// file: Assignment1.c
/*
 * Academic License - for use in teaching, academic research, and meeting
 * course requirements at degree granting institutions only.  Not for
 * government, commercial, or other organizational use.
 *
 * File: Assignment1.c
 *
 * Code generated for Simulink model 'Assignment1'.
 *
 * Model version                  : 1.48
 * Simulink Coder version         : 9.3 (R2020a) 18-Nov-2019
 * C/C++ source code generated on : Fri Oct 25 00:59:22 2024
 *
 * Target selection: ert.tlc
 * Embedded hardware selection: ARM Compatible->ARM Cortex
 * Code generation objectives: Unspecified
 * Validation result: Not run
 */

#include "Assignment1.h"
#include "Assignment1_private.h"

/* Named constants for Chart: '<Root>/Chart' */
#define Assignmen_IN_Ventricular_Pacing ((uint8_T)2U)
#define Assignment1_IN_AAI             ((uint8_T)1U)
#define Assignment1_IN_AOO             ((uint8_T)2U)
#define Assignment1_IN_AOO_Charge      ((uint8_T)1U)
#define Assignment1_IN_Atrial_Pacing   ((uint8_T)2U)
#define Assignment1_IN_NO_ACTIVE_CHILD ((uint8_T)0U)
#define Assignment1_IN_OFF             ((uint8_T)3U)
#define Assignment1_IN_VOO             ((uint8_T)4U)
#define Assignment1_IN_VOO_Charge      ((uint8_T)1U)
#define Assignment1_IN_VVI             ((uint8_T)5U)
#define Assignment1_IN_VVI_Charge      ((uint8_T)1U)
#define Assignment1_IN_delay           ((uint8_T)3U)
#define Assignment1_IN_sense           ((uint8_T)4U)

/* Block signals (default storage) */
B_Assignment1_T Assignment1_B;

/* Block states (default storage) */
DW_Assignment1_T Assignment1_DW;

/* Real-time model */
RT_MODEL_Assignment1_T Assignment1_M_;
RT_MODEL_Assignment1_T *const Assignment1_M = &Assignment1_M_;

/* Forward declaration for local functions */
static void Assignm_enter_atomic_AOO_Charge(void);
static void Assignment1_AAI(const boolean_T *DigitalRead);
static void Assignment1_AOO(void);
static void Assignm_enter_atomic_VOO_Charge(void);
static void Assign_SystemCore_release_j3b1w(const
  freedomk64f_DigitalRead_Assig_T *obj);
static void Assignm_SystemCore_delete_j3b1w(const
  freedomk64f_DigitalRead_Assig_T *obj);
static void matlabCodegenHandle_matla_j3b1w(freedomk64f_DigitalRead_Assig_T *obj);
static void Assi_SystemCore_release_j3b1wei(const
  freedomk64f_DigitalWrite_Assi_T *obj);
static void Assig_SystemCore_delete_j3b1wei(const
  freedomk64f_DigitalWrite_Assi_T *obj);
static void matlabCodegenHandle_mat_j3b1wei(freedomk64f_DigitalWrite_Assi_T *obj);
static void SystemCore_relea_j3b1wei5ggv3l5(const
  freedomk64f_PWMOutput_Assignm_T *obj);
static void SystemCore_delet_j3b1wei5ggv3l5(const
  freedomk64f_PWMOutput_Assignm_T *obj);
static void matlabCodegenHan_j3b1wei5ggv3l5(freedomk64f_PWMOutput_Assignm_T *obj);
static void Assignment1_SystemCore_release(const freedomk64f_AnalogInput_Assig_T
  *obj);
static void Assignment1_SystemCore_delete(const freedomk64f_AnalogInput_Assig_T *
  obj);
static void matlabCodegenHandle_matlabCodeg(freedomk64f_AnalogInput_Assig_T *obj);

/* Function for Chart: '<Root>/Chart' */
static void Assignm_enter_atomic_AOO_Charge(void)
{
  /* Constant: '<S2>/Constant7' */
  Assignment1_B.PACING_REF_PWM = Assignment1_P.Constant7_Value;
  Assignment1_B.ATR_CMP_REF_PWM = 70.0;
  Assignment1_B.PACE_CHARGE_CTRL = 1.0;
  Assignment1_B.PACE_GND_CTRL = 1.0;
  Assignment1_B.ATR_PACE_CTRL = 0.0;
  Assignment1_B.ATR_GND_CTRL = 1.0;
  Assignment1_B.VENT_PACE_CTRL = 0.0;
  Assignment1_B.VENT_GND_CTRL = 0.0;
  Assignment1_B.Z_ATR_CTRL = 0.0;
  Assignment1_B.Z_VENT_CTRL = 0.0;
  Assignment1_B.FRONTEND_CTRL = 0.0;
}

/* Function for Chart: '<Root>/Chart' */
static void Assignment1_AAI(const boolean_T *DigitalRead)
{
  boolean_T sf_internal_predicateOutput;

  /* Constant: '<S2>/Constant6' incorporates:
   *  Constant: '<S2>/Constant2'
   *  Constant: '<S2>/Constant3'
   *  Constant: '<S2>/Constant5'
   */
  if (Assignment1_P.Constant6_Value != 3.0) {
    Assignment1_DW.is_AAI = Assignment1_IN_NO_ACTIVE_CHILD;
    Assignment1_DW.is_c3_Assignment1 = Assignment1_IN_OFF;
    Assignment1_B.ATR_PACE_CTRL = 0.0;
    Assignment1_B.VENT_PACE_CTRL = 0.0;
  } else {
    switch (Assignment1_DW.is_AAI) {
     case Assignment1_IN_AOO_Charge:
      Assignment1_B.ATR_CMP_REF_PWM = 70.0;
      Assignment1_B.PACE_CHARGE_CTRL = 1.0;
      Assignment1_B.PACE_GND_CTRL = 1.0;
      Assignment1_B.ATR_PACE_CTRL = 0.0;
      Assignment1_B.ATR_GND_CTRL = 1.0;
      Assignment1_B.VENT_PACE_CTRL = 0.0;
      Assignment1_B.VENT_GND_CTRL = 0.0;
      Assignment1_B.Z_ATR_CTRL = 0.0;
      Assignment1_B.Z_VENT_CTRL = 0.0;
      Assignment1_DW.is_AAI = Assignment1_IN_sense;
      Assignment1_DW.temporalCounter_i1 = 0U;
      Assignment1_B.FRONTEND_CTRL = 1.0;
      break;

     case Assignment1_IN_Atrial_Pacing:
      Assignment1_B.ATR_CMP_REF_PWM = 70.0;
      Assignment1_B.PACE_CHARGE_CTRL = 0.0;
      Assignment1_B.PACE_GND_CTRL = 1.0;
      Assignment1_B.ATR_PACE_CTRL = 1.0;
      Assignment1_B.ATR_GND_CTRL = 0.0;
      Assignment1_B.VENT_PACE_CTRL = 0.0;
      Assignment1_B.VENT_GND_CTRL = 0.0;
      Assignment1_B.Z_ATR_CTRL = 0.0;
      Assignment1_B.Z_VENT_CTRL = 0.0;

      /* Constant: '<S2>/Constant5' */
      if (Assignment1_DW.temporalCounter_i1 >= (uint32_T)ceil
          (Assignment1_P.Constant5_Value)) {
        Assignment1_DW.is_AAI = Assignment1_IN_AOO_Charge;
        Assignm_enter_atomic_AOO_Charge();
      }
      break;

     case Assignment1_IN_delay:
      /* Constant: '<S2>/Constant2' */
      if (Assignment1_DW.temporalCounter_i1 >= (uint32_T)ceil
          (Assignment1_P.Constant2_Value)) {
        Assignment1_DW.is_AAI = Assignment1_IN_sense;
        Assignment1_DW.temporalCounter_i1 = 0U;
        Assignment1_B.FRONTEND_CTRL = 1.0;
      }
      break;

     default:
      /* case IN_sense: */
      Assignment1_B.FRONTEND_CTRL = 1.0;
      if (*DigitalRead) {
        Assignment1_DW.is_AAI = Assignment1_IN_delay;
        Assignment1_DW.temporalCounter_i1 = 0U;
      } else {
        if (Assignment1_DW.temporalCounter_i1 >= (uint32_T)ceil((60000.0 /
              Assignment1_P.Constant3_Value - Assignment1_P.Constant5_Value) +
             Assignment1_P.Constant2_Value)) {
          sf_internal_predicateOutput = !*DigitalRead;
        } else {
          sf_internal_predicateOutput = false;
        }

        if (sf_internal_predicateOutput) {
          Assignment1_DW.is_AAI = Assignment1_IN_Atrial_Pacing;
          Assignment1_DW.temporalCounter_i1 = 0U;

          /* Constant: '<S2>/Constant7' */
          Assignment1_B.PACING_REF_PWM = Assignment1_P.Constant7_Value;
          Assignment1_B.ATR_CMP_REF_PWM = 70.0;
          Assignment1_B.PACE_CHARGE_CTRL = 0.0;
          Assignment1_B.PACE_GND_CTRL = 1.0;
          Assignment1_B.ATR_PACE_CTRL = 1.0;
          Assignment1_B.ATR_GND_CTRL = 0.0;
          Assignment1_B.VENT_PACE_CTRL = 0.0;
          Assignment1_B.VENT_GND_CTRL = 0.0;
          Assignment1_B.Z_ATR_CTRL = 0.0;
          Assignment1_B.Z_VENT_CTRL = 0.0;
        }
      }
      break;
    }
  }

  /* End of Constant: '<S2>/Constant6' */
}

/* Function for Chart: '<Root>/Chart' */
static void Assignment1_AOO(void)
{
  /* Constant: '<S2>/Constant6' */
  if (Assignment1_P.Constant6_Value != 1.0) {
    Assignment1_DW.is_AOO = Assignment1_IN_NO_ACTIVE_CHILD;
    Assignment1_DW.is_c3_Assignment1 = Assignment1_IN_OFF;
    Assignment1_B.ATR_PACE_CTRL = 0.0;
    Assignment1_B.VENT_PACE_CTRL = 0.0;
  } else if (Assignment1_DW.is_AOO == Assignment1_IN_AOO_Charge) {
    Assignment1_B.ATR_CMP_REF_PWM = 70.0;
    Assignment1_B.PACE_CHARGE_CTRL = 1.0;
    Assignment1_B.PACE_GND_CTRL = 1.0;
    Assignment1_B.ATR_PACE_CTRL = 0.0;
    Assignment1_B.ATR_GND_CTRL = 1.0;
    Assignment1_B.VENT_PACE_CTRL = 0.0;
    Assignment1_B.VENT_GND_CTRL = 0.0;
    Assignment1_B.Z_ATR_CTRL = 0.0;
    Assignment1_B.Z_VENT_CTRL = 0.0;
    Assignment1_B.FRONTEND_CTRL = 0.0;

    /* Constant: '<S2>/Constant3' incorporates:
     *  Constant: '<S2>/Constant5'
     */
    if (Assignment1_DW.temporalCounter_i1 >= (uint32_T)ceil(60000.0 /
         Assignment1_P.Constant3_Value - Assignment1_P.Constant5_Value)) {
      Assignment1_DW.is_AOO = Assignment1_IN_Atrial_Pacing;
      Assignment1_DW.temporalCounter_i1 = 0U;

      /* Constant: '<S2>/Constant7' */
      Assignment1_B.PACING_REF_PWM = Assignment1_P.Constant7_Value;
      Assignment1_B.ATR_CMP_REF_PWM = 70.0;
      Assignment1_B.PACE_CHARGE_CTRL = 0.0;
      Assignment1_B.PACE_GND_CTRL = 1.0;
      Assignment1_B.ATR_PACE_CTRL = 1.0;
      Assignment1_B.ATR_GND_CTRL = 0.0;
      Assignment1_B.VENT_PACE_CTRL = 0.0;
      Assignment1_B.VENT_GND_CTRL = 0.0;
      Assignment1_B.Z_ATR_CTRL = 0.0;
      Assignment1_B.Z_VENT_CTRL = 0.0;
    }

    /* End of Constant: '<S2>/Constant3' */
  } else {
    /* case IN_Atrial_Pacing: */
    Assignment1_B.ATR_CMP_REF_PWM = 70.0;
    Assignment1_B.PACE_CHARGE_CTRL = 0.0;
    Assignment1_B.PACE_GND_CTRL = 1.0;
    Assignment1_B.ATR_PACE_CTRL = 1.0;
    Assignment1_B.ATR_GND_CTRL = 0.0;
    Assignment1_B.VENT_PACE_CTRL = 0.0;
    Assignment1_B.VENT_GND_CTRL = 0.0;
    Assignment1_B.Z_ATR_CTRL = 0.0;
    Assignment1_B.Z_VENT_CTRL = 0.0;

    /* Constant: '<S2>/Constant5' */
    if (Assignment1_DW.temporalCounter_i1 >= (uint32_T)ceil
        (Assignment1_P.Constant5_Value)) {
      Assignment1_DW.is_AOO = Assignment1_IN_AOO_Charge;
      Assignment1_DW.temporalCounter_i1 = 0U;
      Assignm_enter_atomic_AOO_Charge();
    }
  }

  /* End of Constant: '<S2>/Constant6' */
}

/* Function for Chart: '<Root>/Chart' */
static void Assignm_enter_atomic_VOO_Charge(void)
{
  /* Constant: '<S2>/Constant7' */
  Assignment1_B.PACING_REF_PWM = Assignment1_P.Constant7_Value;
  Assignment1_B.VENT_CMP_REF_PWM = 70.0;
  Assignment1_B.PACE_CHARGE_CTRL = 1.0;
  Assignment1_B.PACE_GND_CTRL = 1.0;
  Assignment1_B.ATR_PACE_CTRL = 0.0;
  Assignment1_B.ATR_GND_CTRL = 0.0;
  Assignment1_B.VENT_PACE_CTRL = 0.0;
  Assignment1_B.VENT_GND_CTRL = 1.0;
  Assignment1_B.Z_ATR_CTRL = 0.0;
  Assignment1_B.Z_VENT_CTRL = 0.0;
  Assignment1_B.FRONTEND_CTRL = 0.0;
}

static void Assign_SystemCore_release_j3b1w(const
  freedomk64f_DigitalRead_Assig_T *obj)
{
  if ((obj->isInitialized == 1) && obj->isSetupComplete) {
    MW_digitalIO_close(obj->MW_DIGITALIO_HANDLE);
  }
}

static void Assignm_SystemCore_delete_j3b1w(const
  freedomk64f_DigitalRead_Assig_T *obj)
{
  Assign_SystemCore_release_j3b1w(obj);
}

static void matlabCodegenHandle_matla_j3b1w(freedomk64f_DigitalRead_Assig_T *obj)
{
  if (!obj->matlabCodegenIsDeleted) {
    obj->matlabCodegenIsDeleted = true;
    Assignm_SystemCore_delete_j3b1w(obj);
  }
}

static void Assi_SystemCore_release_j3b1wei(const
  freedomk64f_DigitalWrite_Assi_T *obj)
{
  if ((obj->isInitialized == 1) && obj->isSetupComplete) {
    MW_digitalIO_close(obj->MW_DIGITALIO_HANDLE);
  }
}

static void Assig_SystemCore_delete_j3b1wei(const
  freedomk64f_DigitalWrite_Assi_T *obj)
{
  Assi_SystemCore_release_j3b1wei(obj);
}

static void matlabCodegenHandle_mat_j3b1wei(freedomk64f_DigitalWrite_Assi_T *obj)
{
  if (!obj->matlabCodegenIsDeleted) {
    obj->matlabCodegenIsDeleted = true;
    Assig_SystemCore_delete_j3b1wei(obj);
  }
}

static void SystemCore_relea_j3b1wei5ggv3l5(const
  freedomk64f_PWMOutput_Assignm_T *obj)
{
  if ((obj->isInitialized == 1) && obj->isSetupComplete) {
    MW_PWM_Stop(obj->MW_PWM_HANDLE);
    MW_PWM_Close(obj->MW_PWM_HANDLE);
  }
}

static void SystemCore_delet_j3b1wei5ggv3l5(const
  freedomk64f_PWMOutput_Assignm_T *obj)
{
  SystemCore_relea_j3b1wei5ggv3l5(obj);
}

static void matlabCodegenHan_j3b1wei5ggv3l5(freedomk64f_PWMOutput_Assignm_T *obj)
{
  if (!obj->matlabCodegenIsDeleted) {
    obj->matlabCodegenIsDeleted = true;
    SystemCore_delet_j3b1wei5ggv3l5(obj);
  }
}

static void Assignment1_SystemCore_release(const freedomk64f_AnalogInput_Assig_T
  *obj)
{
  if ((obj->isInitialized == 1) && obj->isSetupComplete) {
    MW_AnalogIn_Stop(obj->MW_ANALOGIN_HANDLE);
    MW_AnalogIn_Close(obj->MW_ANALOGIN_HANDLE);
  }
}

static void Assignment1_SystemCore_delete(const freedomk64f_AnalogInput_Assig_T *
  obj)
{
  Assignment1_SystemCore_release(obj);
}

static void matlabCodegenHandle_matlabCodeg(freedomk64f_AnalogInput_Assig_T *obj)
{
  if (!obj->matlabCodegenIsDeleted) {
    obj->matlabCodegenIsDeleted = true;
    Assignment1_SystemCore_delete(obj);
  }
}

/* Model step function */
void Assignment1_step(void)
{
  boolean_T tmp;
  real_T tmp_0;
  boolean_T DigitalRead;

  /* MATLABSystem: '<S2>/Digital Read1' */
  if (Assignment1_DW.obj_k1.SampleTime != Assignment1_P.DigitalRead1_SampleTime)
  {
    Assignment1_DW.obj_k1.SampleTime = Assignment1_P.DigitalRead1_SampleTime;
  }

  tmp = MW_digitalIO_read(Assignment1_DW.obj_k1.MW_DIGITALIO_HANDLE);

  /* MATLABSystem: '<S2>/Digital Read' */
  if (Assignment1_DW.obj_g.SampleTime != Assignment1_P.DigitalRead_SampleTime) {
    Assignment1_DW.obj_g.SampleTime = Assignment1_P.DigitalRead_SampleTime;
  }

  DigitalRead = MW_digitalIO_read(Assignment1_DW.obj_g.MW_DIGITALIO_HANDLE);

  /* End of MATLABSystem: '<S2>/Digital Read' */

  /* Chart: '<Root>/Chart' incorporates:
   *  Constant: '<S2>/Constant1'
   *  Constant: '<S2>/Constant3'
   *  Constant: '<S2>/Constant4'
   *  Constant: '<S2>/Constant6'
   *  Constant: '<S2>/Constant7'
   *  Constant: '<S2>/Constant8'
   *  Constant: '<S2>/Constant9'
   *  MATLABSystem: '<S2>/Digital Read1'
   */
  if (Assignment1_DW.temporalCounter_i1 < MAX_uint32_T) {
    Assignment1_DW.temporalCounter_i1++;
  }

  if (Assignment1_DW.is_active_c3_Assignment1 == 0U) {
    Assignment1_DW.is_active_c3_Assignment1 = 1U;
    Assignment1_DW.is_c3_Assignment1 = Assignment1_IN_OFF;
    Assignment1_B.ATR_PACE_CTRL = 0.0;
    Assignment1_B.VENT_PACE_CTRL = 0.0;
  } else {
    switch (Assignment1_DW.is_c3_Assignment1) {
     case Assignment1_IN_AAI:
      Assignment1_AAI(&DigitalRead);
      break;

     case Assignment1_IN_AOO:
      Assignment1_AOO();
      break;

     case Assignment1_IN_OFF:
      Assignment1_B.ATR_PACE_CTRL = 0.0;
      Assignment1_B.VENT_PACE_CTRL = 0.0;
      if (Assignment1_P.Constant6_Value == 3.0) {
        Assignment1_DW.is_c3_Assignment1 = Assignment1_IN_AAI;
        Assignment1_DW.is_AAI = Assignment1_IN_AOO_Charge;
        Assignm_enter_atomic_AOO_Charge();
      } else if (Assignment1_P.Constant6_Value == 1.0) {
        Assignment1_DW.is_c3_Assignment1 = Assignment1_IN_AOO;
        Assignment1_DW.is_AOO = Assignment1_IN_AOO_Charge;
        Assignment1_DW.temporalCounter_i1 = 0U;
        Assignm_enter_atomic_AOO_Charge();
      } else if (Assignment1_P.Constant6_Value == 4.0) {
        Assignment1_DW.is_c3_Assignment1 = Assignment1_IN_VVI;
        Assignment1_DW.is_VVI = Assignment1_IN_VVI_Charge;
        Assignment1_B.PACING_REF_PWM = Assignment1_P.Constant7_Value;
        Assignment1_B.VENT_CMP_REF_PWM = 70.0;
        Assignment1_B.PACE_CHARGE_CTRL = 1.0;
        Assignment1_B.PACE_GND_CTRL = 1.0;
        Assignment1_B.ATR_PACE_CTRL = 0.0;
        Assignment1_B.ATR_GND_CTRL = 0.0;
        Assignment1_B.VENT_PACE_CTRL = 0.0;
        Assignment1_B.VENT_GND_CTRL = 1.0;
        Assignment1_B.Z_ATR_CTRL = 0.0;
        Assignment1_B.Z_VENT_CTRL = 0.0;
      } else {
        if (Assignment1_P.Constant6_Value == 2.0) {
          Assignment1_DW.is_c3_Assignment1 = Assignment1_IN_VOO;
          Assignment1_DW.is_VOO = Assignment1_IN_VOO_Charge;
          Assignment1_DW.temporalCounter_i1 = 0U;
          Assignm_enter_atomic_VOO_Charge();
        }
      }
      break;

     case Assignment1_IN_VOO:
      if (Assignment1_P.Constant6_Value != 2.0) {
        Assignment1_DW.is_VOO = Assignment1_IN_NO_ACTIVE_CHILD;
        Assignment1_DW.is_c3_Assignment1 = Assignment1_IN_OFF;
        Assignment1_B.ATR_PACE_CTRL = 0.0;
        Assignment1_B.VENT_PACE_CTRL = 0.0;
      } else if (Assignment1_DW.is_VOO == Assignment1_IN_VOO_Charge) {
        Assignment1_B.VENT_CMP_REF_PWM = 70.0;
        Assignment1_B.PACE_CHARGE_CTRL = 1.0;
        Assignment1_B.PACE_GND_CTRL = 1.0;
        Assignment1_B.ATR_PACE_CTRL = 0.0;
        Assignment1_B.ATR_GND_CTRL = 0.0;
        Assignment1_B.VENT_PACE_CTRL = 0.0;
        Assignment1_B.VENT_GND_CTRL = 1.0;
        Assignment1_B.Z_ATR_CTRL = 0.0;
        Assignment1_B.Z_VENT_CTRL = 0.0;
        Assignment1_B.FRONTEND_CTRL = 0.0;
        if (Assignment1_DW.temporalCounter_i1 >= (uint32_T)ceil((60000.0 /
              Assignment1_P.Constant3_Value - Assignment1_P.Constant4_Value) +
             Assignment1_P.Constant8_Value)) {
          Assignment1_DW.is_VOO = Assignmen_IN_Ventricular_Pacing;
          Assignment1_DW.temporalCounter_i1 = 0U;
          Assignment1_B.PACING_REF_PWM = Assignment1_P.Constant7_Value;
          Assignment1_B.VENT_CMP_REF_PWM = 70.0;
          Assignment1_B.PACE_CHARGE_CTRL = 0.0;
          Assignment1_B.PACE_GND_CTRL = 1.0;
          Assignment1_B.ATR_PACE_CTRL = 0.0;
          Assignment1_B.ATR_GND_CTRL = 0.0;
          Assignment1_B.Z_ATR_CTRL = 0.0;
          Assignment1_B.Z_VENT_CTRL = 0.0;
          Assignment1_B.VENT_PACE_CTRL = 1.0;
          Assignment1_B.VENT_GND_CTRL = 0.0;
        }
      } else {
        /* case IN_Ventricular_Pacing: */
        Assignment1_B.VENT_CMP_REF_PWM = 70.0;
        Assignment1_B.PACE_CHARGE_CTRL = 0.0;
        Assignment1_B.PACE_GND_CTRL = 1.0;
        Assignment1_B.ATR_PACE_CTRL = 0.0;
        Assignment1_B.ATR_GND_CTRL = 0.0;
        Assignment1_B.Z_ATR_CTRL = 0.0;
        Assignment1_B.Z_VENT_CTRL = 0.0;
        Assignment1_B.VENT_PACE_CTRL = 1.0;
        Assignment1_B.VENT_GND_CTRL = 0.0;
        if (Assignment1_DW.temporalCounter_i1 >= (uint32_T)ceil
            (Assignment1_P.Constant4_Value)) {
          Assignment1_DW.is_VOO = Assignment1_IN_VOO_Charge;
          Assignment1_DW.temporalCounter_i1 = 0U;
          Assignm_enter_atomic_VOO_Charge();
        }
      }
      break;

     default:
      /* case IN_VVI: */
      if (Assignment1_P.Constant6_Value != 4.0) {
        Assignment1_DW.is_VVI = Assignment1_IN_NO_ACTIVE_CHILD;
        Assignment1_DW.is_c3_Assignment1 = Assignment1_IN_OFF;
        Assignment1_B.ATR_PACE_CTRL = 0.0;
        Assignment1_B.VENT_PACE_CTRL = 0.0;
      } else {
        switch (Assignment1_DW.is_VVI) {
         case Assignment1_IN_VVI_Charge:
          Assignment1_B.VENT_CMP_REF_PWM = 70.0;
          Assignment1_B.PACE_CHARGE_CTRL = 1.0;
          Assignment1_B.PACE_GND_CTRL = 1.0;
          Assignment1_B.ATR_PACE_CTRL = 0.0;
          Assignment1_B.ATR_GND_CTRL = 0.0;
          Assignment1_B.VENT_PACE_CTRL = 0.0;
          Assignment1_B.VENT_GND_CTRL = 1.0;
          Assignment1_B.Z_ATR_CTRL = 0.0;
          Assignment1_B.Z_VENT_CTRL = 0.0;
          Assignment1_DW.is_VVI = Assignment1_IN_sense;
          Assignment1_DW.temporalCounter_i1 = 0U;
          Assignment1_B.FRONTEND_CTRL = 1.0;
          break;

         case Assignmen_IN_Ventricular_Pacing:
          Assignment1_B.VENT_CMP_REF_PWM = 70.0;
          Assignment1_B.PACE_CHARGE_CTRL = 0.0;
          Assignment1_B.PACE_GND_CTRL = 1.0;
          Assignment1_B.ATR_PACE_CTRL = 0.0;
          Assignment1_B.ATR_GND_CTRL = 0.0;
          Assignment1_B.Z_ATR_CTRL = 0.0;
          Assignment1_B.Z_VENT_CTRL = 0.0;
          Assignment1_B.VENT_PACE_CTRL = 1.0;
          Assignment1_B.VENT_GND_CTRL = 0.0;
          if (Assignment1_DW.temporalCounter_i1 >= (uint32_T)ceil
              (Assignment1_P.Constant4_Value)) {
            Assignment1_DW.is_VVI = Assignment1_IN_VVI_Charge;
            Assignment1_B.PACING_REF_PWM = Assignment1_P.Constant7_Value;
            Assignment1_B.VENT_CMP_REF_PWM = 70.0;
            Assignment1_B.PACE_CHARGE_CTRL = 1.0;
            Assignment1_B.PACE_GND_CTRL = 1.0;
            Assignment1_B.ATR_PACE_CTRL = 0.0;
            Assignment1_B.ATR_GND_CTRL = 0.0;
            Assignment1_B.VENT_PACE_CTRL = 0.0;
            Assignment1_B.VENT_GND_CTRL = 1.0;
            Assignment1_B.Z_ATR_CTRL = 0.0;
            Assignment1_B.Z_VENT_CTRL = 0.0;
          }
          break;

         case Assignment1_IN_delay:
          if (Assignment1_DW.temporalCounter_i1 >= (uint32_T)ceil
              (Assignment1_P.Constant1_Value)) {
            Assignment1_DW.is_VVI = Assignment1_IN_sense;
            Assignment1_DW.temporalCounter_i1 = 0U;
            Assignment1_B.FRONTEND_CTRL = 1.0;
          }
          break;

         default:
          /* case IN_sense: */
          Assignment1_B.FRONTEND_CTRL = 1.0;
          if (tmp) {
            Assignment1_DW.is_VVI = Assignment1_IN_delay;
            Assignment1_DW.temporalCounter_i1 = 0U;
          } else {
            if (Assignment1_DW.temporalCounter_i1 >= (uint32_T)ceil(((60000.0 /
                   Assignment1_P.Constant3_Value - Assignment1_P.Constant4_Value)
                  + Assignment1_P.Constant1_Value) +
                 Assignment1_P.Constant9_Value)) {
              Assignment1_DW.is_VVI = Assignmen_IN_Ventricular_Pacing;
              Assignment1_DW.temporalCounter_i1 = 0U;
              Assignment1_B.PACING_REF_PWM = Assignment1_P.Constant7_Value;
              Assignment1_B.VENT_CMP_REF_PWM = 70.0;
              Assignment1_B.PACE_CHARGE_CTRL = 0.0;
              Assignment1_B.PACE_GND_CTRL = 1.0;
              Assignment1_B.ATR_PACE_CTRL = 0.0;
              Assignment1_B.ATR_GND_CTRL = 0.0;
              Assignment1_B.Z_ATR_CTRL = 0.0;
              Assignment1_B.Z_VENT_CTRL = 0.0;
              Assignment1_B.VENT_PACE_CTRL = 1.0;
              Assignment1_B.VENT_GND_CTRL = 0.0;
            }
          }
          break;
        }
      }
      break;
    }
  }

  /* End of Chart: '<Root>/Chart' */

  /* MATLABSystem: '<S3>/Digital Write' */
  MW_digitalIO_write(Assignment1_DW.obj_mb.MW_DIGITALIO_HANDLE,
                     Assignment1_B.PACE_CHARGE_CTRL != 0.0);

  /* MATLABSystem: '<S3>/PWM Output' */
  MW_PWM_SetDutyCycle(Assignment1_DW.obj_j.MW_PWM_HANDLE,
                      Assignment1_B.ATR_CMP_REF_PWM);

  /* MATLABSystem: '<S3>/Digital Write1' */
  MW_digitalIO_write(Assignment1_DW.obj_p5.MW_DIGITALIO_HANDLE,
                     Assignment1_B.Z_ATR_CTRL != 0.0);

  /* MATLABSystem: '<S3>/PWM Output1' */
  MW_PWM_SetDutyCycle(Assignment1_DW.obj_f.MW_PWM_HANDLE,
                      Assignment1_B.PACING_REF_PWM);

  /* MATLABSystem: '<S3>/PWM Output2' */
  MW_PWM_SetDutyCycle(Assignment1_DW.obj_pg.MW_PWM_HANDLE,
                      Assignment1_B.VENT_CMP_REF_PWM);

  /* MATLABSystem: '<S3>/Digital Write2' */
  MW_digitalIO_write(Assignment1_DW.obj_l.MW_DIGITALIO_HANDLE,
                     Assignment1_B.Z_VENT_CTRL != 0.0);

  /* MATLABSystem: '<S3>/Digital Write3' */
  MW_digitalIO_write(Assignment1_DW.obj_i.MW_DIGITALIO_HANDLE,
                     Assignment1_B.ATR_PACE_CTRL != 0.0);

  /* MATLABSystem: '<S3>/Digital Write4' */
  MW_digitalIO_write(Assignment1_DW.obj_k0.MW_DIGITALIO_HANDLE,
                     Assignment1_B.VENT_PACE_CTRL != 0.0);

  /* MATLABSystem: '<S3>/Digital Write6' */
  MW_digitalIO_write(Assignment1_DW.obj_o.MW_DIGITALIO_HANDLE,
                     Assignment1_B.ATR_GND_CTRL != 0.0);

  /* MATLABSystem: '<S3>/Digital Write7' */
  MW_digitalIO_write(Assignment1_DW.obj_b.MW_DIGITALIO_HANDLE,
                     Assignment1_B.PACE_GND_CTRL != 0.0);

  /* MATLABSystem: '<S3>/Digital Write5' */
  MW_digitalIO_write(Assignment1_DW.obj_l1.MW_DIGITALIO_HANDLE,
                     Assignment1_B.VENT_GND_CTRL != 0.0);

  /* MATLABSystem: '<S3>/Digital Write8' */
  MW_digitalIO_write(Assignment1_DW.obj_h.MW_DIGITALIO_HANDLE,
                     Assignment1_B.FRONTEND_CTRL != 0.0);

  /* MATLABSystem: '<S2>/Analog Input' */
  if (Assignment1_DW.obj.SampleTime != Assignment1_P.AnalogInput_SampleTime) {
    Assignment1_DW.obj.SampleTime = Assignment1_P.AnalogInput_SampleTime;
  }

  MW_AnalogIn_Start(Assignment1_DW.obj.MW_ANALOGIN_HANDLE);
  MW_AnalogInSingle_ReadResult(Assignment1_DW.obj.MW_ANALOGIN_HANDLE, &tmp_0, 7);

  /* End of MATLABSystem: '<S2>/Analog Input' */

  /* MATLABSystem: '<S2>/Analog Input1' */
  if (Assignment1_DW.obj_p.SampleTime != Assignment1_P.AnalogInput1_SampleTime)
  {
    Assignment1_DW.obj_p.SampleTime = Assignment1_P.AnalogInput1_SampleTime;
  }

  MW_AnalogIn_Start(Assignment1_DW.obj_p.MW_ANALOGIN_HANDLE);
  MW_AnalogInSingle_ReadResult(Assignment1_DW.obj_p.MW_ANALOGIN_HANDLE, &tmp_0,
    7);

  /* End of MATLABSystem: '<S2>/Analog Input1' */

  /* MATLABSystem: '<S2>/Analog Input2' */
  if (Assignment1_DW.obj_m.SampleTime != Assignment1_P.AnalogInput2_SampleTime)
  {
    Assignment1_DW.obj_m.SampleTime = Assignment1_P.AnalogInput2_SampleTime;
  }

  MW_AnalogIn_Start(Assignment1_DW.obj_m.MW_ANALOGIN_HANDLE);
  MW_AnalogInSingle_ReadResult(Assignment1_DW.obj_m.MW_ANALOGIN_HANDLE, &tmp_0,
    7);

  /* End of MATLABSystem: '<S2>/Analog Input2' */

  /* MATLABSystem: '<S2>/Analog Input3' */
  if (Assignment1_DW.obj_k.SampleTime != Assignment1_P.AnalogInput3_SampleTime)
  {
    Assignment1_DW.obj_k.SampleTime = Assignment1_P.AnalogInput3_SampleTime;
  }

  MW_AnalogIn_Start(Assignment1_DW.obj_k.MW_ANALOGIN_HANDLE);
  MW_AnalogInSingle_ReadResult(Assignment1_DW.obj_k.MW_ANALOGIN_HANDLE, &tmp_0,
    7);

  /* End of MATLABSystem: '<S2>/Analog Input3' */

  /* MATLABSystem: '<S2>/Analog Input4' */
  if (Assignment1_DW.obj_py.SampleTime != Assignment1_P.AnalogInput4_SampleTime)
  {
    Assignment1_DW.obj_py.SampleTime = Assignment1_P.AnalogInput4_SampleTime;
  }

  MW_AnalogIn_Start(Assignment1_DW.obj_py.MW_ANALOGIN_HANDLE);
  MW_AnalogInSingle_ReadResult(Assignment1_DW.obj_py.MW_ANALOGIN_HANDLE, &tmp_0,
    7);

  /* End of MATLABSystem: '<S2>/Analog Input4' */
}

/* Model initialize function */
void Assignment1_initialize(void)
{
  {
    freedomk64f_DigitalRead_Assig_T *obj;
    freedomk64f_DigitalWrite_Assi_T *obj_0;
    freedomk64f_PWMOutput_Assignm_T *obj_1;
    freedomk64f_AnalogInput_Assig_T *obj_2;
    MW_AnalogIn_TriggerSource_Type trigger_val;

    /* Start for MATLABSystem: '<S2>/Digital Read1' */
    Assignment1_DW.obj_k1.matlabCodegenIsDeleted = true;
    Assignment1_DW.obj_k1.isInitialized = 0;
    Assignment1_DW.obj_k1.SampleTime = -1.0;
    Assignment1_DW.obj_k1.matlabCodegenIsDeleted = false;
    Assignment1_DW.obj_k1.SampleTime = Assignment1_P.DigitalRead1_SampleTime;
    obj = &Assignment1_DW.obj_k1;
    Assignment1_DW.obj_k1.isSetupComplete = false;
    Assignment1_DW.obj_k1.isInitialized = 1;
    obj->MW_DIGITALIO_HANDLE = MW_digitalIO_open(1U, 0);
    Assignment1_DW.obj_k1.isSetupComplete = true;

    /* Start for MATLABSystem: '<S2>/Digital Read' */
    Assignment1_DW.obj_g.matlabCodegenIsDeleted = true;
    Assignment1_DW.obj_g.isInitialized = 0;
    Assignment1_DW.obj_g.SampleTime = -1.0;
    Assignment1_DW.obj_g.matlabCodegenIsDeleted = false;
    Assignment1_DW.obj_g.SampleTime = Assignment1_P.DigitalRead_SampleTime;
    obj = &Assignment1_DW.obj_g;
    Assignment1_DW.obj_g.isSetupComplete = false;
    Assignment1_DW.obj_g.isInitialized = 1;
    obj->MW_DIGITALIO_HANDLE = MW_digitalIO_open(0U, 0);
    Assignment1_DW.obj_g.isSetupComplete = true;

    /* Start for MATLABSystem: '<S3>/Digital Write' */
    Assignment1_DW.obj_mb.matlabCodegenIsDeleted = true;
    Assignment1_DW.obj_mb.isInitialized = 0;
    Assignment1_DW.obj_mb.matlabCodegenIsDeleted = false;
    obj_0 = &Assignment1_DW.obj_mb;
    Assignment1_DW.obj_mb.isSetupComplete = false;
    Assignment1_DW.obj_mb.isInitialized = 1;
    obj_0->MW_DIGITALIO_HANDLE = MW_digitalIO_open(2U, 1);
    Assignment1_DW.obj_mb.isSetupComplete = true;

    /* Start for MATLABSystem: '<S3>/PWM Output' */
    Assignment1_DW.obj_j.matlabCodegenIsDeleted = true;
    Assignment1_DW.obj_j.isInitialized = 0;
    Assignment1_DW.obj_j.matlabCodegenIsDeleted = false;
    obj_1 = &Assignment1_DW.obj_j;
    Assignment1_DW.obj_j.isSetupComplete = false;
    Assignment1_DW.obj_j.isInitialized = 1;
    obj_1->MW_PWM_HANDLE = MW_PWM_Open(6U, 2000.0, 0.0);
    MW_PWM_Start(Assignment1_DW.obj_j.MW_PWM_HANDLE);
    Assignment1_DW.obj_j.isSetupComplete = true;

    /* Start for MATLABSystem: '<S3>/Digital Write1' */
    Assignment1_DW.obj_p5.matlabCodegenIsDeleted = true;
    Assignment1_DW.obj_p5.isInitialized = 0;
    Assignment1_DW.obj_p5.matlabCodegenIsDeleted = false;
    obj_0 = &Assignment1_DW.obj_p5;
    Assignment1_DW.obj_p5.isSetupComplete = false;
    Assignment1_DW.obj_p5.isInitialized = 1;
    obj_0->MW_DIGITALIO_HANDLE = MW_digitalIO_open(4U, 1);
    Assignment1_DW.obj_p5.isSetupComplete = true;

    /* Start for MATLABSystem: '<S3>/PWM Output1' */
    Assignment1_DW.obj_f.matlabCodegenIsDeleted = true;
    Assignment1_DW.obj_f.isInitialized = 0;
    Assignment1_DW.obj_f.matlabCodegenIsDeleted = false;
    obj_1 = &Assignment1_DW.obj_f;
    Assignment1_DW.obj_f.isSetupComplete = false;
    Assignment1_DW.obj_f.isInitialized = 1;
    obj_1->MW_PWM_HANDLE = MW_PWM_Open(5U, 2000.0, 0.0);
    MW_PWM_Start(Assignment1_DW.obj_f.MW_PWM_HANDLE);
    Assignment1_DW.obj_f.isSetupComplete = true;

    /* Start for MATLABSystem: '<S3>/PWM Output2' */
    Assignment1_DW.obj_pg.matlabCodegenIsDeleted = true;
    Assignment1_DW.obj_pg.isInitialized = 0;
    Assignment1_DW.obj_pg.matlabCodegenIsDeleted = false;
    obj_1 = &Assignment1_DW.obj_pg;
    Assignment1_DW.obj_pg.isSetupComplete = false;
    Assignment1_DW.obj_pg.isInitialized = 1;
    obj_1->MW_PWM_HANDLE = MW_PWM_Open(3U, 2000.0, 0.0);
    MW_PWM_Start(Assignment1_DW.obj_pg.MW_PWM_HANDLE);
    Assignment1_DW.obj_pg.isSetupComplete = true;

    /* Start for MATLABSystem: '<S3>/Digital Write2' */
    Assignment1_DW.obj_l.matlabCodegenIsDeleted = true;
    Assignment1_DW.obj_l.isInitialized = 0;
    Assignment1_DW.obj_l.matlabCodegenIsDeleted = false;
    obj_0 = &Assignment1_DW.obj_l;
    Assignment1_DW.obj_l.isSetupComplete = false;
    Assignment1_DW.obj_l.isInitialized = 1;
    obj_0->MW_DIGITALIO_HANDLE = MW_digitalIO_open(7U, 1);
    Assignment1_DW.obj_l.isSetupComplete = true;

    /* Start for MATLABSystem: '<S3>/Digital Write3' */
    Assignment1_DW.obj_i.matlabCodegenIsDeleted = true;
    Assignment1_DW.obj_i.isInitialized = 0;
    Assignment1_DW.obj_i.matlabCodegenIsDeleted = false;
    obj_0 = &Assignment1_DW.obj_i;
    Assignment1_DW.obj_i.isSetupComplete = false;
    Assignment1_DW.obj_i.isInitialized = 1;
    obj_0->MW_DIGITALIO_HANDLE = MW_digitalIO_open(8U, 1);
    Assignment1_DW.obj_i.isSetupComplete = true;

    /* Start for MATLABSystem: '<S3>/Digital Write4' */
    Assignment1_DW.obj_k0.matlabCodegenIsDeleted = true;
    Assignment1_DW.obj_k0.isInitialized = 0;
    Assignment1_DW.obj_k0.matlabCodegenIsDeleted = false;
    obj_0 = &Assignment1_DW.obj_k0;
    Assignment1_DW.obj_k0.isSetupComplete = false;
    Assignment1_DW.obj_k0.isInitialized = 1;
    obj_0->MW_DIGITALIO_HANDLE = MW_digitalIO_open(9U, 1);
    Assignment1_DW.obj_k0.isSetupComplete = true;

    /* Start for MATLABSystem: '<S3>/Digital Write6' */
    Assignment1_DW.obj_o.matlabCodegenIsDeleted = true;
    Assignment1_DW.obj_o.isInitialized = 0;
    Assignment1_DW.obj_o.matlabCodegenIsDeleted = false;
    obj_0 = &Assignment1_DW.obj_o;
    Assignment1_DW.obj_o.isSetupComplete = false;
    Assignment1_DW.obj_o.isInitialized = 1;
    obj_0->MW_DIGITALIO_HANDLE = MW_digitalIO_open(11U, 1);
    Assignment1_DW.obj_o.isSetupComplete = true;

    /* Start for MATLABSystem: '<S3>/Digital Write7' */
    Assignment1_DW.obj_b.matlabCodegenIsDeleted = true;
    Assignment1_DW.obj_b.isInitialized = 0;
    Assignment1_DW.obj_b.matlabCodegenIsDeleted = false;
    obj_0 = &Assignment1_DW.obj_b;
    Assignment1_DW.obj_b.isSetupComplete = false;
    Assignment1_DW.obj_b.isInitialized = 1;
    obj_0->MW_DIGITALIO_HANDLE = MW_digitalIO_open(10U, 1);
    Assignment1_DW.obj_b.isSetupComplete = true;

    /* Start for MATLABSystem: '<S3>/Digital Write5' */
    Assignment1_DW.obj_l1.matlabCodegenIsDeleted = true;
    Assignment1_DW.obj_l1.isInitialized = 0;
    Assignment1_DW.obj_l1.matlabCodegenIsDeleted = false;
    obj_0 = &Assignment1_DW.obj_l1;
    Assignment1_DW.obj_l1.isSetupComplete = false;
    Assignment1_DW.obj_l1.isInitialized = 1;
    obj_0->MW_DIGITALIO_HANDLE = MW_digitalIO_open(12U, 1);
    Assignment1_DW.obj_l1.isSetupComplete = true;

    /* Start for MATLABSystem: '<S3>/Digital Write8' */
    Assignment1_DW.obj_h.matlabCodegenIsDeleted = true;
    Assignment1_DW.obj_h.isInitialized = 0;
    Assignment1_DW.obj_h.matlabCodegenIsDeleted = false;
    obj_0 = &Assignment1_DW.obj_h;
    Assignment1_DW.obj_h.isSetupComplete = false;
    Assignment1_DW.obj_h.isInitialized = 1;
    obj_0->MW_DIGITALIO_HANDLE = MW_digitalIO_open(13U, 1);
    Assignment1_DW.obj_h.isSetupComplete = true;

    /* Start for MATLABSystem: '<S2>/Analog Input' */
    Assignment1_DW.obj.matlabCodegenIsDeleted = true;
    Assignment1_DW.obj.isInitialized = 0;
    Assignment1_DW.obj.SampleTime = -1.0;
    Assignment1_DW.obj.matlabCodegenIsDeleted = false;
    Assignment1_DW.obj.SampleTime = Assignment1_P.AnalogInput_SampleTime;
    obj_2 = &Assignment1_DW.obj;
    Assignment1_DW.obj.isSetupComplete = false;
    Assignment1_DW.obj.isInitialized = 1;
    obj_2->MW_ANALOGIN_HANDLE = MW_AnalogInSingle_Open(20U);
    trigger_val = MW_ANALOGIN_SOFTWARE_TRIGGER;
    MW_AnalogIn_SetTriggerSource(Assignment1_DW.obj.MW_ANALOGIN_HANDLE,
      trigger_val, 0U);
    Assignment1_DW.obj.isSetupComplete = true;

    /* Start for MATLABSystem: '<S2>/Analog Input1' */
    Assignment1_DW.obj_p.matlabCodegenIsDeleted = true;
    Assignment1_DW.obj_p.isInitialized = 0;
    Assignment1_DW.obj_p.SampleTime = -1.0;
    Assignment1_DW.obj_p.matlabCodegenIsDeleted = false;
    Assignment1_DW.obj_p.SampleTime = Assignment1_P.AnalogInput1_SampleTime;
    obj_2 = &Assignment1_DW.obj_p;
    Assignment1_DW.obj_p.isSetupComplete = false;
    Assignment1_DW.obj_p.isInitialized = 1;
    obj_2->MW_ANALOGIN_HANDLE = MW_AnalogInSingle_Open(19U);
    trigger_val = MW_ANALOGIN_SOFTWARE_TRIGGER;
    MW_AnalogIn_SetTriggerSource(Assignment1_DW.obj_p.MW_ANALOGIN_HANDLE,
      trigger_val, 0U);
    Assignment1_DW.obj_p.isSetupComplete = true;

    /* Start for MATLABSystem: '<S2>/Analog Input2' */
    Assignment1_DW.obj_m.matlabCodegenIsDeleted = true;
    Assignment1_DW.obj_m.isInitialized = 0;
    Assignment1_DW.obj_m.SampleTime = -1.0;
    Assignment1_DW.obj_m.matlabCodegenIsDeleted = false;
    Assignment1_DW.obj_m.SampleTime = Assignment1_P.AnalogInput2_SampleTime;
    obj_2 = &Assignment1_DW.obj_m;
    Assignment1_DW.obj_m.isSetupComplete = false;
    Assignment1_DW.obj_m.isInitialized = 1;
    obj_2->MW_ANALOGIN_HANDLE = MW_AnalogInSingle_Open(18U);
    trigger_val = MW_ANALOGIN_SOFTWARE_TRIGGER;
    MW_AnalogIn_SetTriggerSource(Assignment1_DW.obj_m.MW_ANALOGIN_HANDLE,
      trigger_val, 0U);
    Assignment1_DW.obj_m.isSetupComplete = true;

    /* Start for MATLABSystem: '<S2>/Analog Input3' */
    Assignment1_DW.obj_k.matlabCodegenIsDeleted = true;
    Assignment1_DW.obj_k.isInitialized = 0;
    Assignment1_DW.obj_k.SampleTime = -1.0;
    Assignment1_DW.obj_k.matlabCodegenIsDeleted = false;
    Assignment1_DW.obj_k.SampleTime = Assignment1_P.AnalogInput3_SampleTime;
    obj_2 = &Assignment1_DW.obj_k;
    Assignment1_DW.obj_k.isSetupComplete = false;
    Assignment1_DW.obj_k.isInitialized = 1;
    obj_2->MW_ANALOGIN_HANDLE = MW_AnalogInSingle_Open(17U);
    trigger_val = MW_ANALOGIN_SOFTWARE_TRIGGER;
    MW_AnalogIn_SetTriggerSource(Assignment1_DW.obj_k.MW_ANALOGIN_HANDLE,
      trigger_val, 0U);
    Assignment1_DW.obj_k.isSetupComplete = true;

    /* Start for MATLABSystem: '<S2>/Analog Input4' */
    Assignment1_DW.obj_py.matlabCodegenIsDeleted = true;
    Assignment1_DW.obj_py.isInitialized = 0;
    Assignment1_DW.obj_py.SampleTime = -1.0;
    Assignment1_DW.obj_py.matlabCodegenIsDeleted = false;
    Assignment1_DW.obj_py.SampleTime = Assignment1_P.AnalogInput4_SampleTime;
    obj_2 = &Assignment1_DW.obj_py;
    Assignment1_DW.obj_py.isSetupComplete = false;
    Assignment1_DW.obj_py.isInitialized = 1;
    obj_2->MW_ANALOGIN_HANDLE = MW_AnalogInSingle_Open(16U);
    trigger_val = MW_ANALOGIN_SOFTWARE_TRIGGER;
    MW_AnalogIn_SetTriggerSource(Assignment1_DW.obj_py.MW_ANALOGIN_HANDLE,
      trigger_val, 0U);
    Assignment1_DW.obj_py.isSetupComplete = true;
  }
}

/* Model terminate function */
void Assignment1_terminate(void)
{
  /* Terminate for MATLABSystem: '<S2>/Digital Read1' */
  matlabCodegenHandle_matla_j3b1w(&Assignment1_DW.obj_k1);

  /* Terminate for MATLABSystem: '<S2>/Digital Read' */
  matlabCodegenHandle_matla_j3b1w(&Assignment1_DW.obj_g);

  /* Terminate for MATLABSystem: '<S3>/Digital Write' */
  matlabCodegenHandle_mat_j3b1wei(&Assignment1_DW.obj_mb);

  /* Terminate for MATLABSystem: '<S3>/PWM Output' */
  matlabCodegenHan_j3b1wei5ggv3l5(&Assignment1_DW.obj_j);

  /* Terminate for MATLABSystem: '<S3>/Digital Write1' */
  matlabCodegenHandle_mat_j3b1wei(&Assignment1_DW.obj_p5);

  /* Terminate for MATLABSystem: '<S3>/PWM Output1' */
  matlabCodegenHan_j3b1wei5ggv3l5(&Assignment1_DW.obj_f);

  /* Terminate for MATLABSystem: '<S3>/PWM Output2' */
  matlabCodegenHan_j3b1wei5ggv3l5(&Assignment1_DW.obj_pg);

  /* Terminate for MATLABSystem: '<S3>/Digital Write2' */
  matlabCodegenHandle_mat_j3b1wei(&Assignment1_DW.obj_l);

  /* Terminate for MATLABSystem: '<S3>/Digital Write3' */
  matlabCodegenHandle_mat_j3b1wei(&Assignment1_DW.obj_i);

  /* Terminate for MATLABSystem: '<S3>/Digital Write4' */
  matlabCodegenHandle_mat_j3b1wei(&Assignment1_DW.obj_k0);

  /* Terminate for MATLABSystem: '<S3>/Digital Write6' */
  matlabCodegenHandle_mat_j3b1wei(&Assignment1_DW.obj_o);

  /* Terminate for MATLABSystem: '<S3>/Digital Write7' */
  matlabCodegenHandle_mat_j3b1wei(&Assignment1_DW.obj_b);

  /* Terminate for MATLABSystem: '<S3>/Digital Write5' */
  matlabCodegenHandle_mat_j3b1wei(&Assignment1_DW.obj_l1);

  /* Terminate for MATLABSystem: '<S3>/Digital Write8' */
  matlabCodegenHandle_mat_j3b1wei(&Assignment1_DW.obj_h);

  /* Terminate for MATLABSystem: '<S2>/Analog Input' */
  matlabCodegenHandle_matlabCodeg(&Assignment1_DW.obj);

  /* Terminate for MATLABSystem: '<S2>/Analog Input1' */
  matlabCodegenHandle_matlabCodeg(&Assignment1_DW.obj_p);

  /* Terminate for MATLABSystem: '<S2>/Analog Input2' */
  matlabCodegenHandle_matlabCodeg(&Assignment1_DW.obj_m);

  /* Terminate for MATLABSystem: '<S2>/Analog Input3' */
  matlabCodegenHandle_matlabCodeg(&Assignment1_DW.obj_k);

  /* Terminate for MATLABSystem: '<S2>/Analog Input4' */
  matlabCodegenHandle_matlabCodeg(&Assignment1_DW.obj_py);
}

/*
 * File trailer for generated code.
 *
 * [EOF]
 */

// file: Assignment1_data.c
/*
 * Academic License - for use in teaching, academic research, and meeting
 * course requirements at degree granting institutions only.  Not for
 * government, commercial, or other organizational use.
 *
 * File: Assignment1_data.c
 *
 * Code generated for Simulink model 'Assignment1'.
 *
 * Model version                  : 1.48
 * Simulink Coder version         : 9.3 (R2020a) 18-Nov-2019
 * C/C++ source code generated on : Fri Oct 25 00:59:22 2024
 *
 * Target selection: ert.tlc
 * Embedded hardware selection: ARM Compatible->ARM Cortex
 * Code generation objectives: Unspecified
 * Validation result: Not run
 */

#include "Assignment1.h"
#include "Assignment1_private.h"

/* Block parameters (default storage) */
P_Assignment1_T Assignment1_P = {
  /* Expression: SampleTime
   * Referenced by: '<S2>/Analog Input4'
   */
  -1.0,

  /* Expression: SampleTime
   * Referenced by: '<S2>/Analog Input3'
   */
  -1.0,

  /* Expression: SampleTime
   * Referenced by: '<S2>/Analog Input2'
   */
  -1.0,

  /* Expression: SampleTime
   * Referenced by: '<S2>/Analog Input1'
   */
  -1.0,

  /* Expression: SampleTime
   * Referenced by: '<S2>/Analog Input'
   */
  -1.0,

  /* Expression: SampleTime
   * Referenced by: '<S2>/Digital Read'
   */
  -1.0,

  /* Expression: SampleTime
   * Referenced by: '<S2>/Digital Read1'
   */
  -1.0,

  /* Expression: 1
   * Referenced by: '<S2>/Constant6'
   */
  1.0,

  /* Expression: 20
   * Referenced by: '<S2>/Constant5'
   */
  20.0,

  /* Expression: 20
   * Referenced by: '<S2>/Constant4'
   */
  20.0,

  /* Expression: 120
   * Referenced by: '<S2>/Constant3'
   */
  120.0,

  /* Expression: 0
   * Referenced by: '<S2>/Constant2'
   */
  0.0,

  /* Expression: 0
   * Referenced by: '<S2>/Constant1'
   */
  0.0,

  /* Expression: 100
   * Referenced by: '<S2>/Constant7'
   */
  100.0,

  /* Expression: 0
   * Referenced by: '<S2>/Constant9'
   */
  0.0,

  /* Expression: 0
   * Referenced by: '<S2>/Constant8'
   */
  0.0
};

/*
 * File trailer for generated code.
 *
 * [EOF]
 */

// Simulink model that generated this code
simulink model "Assignment1"  (R2020a)
settings: Solver=FixedStepAuto  StartTime=0.0  StopTime=5  FixedStep=1e-3  RelTol=1e-3  EnableMultiTasking=on
model workspace (MAT data in the model file):
  ATR_CMP_REF_PWM_PERCENTAGE = 50
  PACING_REF_PWM_DUTY_PERCENTAGE = 50
  VENT_CMP_REF_PWM_PERCENTAGE = 50
undefined symbols (not defined in the file or in its folder): A0, A1, A2, A3, A4, D0, D1, PTB10, PTB11, PTB2, PTB3, PTC11, PTC16, PTC17
libraries: frdmk64flib x7

== system Assignment1 ==
  Chart : Stateflow chart  TreatAsAtomicUnit=on
  Input : Subsystem
  Output : Subsystem  ReferencedSubsystem=k64f_subsystem
  wires:
  Input/1(mode) -> Chart/1(mode)
  Chart/10(PACING_REF_PWM) -> Output/4
  Input/2(atrial_pulse_width) -> Chart/2(atrial_pulse_width)
  Input/3(ventricular_pulse_width) -> Chart/3(ventricular_pulse_width)
  Chart/8(Z_ATR_CTRL) -> Output/3
  Chart/7(Z_VENT_CTRL) -> Output/6
  Chart/4(ATR_GND_CTRL) -> Output/9
  Chart/3(ATR_PACE_CTRL) -> Output/7
  Chart/5(VENT_GND_CTRL) -> Output/11
  Chart/2(VENT_PACE_CTRL) -> Output/8
  Chart/1(PACE_CHARGE_CTRL) -> Output/1
  Chart/6(PACE_GND_CTRL) -> Output/10
  Chart/11(ATR_CMP_REF_PWM) -> Output/2
  Chart/12(VENT_CMP_REF_PWM) -> Output/5
  Chart/9(FRONTEND_CTRL) -> Output/12
  Input/6(BPM) -> Chart/6(BPM)
  Input/4(VENT_CMP_DETECT) -> Chart/4(VENT_CMP_DETECT)
  Input/5(ATR_CMP_DETECT) -> Chart/5(ATR_CMP_DETECT)
  Input/7(ARP) -> Chart/7(ARP)
  Input/8(VRP) -> Chart/8(VRP)
  Input/9(amplitude) -> Chart/9(amplitude)
  Input/10(URL) -> Chart/10(URL)
  Input/11(LRL) -> Chart/11(LRL)

== system Assignment1/Input ==
  note: Ventricular Pins
  note: Atrial Pins
  note: Impedance Pins
  note: Parameter Pins
  Analog Input : frdmk64flib/Analog Input  Whichpin=PTC11 (A4)  SampleTime=-1
  Analog Input1 : frdmk64flib/Analog Input  Whichpin=PTB11 (A3)  SampleTime=-1
  Analog Input2 : frdmk64flib/Analog Input  Whichpin=PTB10 (A2)  SampleTime=-1
  Analog Input3 : frdmk64flib/Analog Input  Whichpin=PTB3 (A1)  SampleTime=-1
  Analog Input4 : frdmk64flib/Analog Input  Whichpin=PTB2 (A0)  SampleTime=-1
  Constant{1..2,8..9} (4 alike) : Constant  Value=0
  Constant3 : Constant  Value=120
  Constant4 : Constant  Value=20
  Constant5 : Constant  Value=20
  Constant6 : Constant
  Constant7 : Constant  Value=100
  Digital Read : frdmk64flib/Digital Read  Whichpin=PTC16 (D0)  SampleTime=-1
  Digital Read1 : frdmk64flib/Digital Read  Whichpin=PTC17 (D1)  SampleTime=-1
  mode : Outport
  atrial_pulse_width : Outport  Port=2
  ventricular_pulse_width : Outport  Port=3
  VENT_CMP_DETECT : Outport  Port=4
  ATR_CMP_DETECT : Outport  Port=5
  BPM : Outport  Port=6
  ARP : Outport  Port=7
  VRP : Outport  Port=8
  amplitude : Outport  Port=9
  URL : Outport  Port=10
  LRL : Outport  Port=11
  VENT_RECT_SIGNAL : Outport  Port=12
  ATR_RECT_SIGNAL : Outport  Port=13
  Z_SIGNAL : Outport  Port=14
  VENT_SIGNAL : Outport  Port=15
  ATR_SIGNAL : Outport  Port=16
  wires:
  Analog Input4/1 -> ATR_SIGNAL/1
  Analog Input2/1 -> Z_SIGNAL/1
  Analog Input3/1 -> VENT_SIGNAL/1
  Analog Input/1 -> VENT_RECT_SIGNAL/1
  Digital Read1/1 -> VENT_CMP_DETECT/1
  Digital Read/1 -> ATR_CMP_DETECT/1
  Analog Input1/1 -> ATR_RECT_SIGNAL/1
  Constant6/1 -> mode/1
  Constant5/1 -> atrial_pulse_width/1
  Constant4/1 -> ventricular_pulse_width/1
  Constant3/1 -> BPM/1
  Constant1/1 -> VRP/1
  Constant2/1 -> ARP/1
  Constant7/1 -> amplitude/1
  Constant9/1 -> URL/1
  Constant8/1 -> LRL/1

== stateflow chart Assignment1/Chart ==
  state AAI
    state delay
    state AOO_Charge
      entry:
      PACING_REF_PWM = amplitude;
      ATR_CMP_REF_PWM = 70;
      PACE_CHARGE_CTRL = 1;
      PACE_GND_CTRL = 1;
      ATR_PACE_CTRL = 0;
      ATR_GND_CTRL = 1;
      VENT_PACE_CTRL = 0;
      VENT_GND_CTRL = 0;
      Z_ATR_CTRL = 0;
      Z_VENT_CTRL =0;
      FRONTEND_CTRL = 0;
    state sense
      entry:
      FRONTEND_CTRL = 1;
    state Atrial_Pacing
      entry:
      PACING_REF_PWM = amplitude;
      ATR_CMP_REF_PWM = 70;
      PACE_CHARGE_CTRL = 0;
      PACE_GND_CTRL = 1;
      ATR_PACE_CTRL = 1;
      ATR_GND_CTRL = 0;
      VENT_PACE_CTRL = 0;
      VENT_GND_CTRL = 0;
      Z_ATR_CTRL = 0;
      Z_VENT_CTRL = 0;
    (default) -> AAI.AOO_Charge
    AAI.delay -> AAI.sense : [after(ARP,msec)]
    AAI.sense -> AAI.delay [order 1] : [ATR_CMP_DETECT == 1]
    AAI.AOO_Charge -> AAI.sense
    AAI.sense -> AAI.Atrial_Pacing [order 2] : [after((60000/BPM) - atrial_pulse_width + ARP,msec) && ATR_CMP_DETECT == 0]
    AAI.Atrial_Pacing -> AAI.AOO_Charge : [after(atrial_pulse_width,msec)]
  state VVI
    state delay
    state VVI_Charge
      entry:
      PACING_REF_PWM = amplitude;
      VENT_CMP_REF_PWM = 70;
      PACE_CHARGE_CTRL = 1;
      PACE_GND_CTRL = 1;
      ATR_PACE_CTRL = 0;
      ATR_GND_CTRL = 0;
      VENT_PACE_CTRL = 0;
      VENT_GND_CTRL = 1;
      Z_ATR_CTRL = 0;
      Z_VENT_CTRL =0;
    state sense
      entry:
      FRONTEND_CTRL = 1;
    state Ventricular_Pacing
      entry:
      PACING_REF_PWM = amplitude;
      VENT_CMP_REF_PWM = 70;
      PACE_CHARGE_CTRL = 0;
      PACE_GND_CTRL = 1;
      ATR_PACE_CTRL = 0;
      ATR_GND_CTRL = 0;
      Z_ATR_CTRL = 0;
      Z_VENT_CTRL = 0;
      VENT_PACE_CTRL = 1;
      VENT_GND_CTRL = 0;
    (default) -> VVI_Charge
    VVI.delay -> VVI.sense : [after(VRP,msec)]
    VVI.sense -> VVI.delay [order 1] : [VENT_CMP_DETECT == 1]
    VVI_Charge -> VVI.sense
    VVI.sense -> VVI.Ventricular_Pacing [order 2] : [after((60000/BPM) - ventricular_pulse_width + VRP + URL,msec) && VENT_CMP_DETECT == 0]
    VVI.Ventricular_Pacing -> VVI_Charge : [after(ventricular_pulse_width,msec)]
  state AOO
    state AOO_Charge
      entry:
      PACING_REF_PWM = amplitude;
      ATR_CMP_REF_PWM = 70;
      PACE_CHARGE_CTRL = 1;
      PACE_GND_CTRL = 1;
      ATR_PACE_CTRL = 0;
      ATR_GND_CTRL = 1;
      VENT_PACE_CTRL = 0;
      VENT_GND_CTRL = 0;
      Z_ATR_CTRL = 0;
      Z_VENT_CTRL =0;
      FRONTEND_CTRL = 0;
    state Atrial_Pacing
      entry:
      PACING_REF_PWM = amplitude;
      ATR_CMP_REF_PWM = 70;
      PACE_CHARGE_CTRL = 0;
      PACE_GND_CTRL = 1;
      ATR_PACE_CTRL = 1;
      ATR_GND_CTRL = 0;
      VENT_PACE_CTRL = 0;
      VENT_GND_CTRL = 0;
      Z_ATR_CTRL = 0;
      Z_VENT_CTRL = 0;
    (default) -> AOO.AOO_Charge
    AOO.AOO_Charge -> AOO.Atrial_Pacing : [after((60000/BPM) - atrial_pulse_width,msec)]
    AOO.Atrial_Pacing -> AOO.AOO_Charge : [after(atrial_pulse_width,msec)]
  state OFF
    entry:
    ATR_PACE_CTRL = 0;
    VENT_PACE_CTRL = 0;
  state VOO
    state VOO_Charge
      entry:
      PACING_REF_PWM = amplitude;
      VENT_CMP_REF_PWM = 70;
      PACE_CHARGE_CTRL = 1;
      PACE_GND_CTRL = 1;
      ATR_PACE_CTRL = 0;
      ATR_GND_CTRL = 0;
      VENT_PACE_CTRL = 0;
      VENT_GND_CTRL = 1;
      Z_ATR_CTRL = 0;
      Z_VENT_CTRL =0;
      FRONTEND_CTRL = 0;
    state Ventricular_Pacing
      entry:
      PACING_REF_PWM = amplitude;
      VENT_CMP_REF_PWM = 70;
      PACE_CHARGE_CTRL = 0;
      PACE_GND_CTRL = 1;
      ATR_PACE_CTRL = 0;
      ATR_GND_CTRL = 0;
      Z_ATR_CTRL = 0;
      Z_VENT_CTRL = 0;
      VENT_PACE_CTRL = 1;
      VENT_GND_CTRL = 0;
    (default) -> VOO_Charge
    VOO_Charge -> VOO.Ventricular_Pacing : [after((60000/BPM) - ventricular_pulse_width +LRL,msec)]
    VOO.Ventricular_Pacing -> VOO_Charge : [after(ventricular_pulse_width,msec)]
  AAI -> OFF : [mode ~= 3]
  OFF -> AAI [order 1] : [mode == 3]
  (default) -> OFF
  AOO -> OFF : [mode ~= 1]
  OFF -> VVI [order 3] : [mode == 4]
  OFF -> AOO [order 2] : [mode == 1]
  VVI -> OFF : [mode ~= 4]
  VOO -> OFF : [mode ~= 2]
  OFF -> VOO [order 4] : [mode == 2]
  data: PACE_CHARGE_CTRL output; VENT_PACE_CTRL output; ATR_PACE_CTRL output; ATR_GND_CTRL output; VENT_GND_CTRL output; PACE_GND_CTRL output; mode input; Z_VENT_CTRL output; Z_ATR_CTRL output; atrial_pulse_width input; ventricular_pulse_width input; VENT_CMP_DETECT input; ATR_CMP_DETECT input; FRONTEND_CTRL output; BPM input; PACING_REF_PWM output; ATR_CMP_REF_PWM output; VENT_CMP_REF_PWM output; ARP input; VRP input; amplitude input; URL input; LRL input
